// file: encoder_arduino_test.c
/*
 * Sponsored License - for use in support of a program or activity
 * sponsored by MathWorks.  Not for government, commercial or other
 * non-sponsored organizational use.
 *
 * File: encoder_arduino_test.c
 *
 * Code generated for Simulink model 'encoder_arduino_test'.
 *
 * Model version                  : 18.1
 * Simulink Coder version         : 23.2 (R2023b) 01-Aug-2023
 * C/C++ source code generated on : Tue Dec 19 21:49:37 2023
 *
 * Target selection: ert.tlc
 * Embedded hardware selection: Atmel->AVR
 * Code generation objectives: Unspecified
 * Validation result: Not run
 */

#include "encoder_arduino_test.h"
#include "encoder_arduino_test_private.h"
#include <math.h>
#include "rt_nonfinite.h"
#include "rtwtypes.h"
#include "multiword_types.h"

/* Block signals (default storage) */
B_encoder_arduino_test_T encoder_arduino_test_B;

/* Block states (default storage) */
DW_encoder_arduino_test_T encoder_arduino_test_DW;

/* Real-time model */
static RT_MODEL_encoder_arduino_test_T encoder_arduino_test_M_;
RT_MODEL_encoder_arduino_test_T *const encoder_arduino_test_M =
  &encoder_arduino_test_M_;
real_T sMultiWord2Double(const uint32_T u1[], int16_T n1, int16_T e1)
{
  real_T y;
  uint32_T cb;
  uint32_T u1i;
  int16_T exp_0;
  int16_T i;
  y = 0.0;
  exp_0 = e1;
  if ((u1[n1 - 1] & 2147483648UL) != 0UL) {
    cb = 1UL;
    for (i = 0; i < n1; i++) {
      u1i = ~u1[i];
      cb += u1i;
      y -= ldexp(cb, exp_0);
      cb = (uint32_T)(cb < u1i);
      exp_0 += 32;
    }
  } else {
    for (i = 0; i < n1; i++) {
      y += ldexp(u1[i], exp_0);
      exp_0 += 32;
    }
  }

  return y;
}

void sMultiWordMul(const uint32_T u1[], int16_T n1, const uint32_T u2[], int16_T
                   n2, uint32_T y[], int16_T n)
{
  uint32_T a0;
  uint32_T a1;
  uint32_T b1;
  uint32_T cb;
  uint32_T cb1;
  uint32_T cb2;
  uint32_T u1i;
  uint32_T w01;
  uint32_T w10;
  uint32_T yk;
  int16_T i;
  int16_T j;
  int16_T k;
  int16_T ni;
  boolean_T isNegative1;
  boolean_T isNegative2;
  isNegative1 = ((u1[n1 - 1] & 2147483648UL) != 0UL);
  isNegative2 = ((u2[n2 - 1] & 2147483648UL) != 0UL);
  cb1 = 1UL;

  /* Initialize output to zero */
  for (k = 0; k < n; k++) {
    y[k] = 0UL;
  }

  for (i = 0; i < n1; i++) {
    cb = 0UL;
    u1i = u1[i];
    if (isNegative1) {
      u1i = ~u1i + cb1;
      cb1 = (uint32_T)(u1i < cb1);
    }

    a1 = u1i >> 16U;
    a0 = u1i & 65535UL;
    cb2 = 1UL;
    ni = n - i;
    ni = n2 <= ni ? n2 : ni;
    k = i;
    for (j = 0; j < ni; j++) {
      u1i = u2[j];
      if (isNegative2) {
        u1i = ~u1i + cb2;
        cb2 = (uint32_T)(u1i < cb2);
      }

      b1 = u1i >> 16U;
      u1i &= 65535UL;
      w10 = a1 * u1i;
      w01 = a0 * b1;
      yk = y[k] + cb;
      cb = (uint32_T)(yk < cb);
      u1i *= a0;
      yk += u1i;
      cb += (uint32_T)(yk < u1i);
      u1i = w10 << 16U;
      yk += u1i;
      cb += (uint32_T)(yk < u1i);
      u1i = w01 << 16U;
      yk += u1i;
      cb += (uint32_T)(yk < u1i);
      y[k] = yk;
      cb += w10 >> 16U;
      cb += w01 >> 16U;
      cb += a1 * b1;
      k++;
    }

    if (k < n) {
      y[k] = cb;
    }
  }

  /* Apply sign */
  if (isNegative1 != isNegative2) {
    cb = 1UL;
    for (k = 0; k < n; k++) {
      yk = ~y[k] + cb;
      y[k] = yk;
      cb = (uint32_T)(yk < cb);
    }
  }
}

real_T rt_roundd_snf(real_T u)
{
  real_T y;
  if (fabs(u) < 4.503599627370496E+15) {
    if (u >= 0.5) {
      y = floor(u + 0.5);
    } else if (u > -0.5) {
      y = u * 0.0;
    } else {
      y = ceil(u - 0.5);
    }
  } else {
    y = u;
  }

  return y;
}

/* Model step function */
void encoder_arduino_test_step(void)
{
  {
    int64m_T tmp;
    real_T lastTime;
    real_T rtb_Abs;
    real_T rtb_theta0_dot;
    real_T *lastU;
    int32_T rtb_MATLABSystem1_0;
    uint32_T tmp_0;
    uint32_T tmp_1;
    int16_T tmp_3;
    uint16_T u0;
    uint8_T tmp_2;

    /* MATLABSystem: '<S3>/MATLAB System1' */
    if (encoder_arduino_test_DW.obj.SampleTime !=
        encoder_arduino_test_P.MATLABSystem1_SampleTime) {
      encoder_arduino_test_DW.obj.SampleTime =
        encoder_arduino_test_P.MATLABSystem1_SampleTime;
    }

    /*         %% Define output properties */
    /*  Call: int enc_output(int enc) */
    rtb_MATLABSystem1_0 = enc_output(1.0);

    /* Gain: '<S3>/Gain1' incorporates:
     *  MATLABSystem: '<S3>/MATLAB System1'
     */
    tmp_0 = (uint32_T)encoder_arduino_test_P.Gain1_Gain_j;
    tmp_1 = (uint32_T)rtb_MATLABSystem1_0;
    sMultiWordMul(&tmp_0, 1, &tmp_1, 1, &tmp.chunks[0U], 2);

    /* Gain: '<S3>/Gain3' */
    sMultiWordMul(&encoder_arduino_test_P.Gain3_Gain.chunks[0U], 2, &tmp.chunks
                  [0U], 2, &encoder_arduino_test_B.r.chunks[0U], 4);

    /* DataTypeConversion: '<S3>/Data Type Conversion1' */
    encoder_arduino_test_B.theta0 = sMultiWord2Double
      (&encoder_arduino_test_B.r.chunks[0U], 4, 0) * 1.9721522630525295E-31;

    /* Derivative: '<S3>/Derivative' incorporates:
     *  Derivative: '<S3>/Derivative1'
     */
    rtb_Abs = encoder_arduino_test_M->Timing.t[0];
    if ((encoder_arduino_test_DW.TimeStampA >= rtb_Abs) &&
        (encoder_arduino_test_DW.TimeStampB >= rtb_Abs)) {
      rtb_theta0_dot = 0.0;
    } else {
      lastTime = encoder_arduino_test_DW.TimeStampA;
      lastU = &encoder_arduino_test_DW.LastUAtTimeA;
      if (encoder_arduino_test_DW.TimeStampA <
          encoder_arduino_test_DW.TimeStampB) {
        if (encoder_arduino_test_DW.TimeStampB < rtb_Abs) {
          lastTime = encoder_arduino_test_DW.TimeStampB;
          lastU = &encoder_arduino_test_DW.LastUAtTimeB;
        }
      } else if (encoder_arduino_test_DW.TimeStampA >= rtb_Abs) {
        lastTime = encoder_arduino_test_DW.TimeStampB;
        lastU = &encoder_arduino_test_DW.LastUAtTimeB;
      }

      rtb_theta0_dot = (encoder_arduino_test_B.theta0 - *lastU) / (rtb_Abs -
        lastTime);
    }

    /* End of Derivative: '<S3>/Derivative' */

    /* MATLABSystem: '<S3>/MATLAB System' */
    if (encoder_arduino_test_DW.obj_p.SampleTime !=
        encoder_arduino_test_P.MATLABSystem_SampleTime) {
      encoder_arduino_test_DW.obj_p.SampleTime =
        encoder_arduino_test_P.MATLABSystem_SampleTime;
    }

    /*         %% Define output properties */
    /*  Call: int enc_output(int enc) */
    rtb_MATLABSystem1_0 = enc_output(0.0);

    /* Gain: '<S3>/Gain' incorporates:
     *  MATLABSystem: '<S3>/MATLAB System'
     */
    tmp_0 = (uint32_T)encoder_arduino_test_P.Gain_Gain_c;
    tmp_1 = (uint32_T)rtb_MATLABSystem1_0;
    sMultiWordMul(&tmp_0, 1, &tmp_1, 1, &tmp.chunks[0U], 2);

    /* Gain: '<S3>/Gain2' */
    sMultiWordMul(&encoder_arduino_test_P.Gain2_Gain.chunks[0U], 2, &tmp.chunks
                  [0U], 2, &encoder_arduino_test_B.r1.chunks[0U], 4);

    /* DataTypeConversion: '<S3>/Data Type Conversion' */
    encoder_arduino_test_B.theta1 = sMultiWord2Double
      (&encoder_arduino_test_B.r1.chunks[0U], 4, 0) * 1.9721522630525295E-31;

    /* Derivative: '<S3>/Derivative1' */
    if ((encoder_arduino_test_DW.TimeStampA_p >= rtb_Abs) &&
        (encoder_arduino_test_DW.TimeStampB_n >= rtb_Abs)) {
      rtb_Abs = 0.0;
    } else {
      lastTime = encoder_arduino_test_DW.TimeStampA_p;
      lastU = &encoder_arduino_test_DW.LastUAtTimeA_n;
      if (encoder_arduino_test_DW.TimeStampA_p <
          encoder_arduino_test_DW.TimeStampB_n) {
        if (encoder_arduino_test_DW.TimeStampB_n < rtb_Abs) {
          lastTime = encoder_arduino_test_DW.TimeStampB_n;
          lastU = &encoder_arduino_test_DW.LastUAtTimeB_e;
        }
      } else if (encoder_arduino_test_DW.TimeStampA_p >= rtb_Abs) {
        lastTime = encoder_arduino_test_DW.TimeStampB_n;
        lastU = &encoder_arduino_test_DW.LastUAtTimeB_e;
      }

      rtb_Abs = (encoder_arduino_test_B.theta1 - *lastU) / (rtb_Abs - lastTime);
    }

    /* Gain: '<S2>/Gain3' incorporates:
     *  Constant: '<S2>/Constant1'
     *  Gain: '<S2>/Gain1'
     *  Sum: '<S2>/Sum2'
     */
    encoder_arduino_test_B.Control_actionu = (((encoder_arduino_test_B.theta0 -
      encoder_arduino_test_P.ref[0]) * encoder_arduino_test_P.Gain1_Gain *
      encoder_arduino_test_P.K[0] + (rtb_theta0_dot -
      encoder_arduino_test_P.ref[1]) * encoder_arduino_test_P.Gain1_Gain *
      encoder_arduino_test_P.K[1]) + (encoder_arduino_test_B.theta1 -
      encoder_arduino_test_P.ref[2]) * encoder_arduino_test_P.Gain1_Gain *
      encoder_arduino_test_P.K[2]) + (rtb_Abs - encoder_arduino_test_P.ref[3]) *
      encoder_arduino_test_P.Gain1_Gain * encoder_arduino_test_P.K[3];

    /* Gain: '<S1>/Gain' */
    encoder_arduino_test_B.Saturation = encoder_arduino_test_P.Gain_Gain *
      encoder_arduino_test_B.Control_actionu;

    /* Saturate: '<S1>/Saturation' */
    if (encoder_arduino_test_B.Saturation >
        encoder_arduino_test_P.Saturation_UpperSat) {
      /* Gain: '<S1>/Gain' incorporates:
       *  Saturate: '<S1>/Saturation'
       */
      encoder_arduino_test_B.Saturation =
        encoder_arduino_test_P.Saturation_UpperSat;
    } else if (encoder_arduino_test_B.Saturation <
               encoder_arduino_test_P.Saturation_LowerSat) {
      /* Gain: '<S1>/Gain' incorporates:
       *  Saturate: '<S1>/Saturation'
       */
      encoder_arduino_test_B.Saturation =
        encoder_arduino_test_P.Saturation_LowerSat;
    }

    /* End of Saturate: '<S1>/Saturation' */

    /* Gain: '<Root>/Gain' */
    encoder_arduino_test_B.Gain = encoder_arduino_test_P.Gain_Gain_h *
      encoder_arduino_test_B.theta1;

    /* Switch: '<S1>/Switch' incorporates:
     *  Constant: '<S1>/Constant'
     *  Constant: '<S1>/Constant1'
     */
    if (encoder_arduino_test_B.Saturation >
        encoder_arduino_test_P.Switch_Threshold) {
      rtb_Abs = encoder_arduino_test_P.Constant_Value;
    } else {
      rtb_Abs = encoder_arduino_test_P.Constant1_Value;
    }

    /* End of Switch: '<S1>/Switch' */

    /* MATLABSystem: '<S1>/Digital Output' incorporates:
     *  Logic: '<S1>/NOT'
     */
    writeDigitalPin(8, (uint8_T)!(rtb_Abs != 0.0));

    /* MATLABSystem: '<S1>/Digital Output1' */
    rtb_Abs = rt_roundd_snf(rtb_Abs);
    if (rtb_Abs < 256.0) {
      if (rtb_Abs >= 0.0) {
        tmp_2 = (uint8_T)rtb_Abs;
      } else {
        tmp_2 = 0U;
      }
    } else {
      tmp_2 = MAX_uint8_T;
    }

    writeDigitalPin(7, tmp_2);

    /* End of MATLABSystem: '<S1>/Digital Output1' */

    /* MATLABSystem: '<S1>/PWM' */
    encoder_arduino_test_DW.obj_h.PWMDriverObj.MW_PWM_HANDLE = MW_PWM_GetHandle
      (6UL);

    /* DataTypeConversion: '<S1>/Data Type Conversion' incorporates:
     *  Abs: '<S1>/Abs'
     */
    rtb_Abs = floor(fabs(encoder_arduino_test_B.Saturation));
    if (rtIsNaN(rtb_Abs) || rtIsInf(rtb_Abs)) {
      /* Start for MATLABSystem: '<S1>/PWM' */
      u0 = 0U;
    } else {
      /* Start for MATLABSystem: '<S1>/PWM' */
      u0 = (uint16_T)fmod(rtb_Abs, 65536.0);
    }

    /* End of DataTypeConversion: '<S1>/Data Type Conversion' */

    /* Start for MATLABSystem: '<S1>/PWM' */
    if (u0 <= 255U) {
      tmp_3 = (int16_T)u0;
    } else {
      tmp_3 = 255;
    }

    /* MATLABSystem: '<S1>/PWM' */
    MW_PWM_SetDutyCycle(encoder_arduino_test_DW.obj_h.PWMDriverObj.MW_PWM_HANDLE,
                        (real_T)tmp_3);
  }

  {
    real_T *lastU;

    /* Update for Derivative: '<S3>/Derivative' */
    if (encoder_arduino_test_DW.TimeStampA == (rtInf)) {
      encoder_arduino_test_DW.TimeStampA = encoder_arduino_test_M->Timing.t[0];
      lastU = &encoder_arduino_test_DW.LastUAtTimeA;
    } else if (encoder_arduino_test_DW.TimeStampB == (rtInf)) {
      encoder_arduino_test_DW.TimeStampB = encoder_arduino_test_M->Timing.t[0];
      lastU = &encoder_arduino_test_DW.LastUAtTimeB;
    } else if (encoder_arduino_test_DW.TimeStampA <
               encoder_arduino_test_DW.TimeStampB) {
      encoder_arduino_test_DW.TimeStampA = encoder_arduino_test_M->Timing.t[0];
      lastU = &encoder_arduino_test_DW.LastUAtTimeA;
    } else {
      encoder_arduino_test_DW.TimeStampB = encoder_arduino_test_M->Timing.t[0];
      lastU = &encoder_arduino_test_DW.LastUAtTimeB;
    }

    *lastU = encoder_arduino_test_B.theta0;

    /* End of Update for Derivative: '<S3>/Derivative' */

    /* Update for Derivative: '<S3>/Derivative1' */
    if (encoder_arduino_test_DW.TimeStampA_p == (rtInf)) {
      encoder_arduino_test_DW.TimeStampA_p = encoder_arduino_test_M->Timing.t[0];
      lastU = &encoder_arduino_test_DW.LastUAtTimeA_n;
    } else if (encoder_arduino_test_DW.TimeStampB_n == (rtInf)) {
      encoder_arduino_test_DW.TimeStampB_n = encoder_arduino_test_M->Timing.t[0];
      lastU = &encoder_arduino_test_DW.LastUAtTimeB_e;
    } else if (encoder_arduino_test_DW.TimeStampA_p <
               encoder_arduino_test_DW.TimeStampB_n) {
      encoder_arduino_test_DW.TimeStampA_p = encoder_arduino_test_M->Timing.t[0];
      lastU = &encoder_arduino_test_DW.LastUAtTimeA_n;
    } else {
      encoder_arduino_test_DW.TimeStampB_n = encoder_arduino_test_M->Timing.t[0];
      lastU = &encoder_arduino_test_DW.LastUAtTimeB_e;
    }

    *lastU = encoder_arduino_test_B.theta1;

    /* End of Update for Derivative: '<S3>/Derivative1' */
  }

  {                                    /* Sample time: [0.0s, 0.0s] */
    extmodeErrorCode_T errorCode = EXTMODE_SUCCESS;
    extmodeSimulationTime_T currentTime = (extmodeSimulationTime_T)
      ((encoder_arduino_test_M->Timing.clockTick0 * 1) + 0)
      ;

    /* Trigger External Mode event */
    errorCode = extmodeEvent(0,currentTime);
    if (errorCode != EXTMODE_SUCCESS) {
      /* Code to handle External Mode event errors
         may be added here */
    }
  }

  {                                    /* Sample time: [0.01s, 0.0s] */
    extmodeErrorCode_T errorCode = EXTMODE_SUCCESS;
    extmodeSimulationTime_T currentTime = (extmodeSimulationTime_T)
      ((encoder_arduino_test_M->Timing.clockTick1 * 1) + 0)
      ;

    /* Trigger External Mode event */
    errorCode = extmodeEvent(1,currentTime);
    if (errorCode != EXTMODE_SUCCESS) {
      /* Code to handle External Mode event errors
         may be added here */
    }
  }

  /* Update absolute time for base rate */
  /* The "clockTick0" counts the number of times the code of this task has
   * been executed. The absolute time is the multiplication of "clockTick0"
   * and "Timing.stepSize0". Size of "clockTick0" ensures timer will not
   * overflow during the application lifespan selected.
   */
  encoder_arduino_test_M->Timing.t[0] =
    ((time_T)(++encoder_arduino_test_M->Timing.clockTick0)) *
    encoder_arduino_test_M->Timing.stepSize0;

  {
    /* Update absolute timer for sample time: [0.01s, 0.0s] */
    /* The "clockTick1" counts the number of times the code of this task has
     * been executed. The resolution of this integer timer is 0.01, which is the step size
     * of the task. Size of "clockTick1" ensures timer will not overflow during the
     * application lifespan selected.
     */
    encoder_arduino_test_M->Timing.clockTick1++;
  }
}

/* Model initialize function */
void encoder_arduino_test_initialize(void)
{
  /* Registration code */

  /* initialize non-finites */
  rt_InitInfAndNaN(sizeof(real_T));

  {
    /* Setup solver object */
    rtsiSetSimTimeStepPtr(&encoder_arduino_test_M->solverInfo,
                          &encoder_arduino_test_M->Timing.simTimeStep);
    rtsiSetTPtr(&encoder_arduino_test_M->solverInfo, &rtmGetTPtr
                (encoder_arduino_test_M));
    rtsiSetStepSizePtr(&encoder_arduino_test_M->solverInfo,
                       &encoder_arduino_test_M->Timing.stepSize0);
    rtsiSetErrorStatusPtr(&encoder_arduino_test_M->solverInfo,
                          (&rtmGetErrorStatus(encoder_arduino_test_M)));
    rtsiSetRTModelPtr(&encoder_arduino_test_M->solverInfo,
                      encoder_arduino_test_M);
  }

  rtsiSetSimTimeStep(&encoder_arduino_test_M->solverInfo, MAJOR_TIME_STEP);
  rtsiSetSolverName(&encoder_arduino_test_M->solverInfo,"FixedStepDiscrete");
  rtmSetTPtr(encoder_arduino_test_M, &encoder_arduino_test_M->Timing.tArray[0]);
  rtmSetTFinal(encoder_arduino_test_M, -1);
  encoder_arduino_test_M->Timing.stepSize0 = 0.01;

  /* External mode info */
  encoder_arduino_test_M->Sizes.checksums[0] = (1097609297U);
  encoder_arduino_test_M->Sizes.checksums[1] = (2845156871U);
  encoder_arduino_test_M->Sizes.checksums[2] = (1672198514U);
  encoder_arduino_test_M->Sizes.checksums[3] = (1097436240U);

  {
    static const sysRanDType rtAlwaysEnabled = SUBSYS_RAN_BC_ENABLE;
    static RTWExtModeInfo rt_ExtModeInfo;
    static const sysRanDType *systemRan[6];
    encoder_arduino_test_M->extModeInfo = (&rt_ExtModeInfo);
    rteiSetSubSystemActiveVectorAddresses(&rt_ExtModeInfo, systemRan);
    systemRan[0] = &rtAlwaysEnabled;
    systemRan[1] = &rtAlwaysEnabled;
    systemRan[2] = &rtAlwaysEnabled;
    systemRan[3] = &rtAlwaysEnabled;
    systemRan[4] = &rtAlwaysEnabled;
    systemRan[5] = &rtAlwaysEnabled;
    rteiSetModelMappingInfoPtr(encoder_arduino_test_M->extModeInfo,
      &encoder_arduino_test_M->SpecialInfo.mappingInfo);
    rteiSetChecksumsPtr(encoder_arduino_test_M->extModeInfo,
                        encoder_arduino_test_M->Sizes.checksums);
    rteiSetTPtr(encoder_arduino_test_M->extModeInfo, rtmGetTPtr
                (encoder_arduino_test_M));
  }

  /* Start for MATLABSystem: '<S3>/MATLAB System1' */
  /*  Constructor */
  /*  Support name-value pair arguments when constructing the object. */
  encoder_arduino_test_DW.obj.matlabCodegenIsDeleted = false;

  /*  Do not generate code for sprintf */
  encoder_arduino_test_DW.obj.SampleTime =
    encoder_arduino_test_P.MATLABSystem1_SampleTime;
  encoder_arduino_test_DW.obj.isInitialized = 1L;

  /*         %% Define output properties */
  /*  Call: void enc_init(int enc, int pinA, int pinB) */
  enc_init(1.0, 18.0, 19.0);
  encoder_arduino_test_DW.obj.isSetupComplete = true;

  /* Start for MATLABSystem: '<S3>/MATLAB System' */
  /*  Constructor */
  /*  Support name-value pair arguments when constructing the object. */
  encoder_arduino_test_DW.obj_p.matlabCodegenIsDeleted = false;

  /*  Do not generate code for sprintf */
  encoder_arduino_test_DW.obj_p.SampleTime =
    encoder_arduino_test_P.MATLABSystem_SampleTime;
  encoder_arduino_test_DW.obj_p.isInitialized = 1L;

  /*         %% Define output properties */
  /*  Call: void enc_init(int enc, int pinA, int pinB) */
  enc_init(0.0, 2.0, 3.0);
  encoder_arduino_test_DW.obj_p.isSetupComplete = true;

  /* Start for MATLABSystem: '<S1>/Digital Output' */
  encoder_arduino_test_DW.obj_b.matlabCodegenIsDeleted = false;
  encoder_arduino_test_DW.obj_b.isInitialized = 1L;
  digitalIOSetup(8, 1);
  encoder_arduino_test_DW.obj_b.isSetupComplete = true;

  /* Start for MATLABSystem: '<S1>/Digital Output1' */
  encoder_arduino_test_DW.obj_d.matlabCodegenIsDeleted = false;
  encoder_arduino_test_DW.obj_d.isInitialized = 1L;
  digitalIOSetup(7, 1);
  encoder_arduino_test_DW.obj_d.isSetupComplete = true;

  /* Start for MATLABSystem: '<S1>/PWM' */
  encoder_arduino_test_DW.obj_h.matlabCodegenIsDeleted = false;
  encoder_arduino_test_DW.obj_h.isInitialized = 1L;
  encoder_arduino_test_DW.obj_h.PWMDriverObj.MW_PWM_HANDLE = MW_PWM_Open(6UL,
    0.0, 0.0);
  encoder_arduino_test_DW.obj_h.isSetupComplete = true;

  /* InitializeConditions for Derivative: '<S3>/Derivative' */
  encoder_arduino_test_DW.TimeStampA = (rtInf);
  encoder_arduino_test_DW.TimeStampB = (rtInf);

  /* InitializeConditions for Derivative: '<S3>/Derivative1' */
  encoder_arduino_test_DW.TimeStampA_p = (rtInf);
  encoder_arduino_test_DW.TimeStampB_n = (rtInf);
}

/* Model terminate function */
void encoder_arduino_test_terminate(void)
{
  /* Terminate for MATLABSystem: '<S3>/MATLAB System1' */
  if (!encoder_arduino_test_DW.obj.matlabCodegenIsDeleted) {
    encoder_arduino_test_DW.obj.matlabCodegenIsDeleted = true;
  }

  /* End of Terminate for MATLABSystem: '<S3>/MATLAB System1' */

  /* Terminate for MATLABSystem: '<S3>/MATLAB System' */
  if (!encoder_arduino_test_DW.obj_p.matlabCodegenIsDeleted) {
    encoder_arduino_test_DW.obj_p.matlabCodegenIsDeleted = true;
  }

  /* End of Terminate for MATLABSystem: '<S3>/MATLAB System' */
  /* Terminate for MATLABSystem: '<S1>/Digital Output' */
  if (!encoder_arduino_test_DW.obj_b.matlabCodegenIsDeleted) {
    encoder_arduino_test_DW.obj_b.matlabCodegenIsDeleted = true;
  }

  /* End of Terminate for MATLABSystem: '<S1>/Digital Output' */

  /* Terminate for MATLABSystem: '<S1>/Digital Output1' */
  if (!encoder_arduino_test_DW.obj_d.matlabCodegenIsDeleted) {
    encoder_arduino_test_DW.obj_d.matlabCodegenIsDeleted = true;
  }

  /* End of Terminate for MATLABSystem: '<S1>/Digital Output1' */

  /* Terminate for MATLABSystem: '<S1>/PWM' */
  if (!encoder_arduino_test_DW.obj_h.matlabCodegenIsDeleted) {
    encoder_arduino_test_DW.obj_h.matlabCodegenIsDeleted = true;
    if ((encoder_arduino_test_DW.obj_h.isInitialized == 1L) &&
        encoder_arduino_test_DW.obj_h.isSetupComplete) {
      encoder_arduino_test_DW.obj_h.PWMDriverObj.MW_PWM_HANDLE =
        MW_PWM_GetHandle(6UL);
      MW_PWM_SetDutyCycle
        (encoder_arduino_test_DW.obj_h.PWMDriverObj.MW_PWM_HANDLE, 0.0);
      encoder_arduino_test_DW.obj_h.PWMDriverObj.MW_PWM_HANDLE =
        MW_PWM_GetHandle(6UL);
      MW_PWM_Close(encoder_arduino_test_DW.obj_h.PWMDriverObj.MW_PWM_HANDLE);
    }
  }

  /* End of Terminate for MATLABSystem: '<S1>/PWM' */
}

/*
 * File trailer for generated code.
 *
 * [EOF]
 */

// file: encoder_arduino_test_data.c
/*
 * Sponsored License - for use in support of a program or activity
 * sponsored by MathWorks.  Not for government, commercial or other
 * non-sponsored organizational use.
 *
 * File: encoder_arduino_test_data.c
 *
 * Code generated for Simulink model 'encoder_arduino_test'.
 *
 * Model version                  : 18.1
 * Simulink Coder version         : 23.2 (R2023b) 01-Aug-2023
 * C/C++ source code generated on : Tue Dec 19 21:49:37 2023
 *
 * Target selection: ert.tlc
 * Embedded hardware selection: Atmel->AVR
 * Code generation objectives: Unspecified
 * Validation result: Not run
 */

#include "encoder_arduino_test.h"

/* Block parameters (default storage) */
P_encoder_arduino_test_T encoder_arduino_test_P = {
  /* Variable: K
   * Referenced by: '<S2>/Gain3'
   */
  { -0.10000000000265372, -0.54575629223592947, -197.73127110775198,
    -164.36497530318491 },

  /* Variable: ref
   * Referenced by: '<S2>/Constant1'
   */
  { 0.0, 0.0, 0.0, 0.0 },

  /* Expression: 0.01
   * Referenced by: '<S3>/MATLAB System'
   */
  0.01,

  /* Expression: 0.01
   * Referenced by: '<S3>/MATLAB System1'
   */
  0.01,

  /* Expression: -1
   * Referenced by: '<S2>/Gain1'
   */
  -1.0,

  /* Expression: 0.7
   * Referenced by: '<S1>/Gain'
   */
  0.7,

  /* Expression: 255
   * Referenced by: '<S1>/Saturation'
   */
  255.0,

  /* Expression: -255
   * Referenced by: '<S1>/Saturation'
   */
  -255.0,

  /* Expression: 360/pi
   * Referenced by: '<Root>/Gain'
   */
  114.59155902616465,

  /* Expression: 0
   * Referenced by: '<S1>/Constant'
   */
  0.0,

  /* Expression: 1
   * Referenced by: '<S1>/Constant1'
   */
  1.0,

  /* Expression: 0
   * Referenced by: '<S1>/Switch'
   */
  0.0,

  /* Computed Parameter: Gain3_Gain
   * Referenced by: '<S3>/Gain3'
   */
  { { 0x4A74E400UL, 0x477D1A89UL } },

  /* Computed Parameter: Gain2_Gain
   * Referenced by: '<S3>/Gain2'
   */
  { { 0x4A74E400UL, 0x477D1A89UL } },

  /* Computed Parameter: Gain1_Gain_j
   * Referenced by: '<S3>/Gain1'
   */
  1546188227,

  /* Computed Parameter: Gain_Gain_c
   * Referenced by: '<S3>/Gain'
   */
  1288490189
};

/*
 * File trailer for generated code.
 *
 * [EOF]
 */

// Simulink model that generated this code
simulink model "encoder_arduino_test"  (R2023b)
settings: Solver=ode3  StartTime=0.0  StopTime=inf  FixedStep=0.01  RelTol=1e-3  EnableMultiTasking=on
undefined symbols (not defined in the file): K, ref
libraries: arduinolib x3

== system encoder_arduino_test ==
  Arduino harduare drive : Subsystem
  Controller : Subsystem
  Demux : Demux
  Gain : Gain  Gain=360/pi
  Scope : Scope  NumInputPorts=2
  States Reading : Subsystem
  wires:
  States Reading/1(State Vector X) -> Demux/1, Controller/1(State Vector X)  "State Vector X"
  Controller/1(Contro Action u) -> Arduino harduare drive/1(Contro Action u)
  Arduino harduare drive/1(Signed Pwm) -> Scope/1
  Demux/3 -> Gain/1
  Gain/1 -> Scope/2

== system encoder_arduino_test/Arduino harduare drive ==
  note: zero
  Contro Action u : Inport
  Abs : Abs  SaturateOnIntegerOverflow=off
  Constant : Constant  Value=0
  Constant1 : Constant
  Data Type Conversion : DataTypeConversion  OutDataTypeStr=uint16  SaturateOnIntegerOverflow=off  RndMeth=Floor
  Digital Output : arduinolib/Digital Output  pinNumber=8  Direction=output  blockPlatform=arduino
  Digital Output1 : arduinolib/Digital Output  pinNumber=7  Direction=output  blockPlatform=arduino
  Gain : Gain  Gain=0.7
  NOT : Logic  Operator=NOT  IconShape=distinctive  AllPortsSameDT=off  OutDataTypeStr=boolean
  PWM : arduinolib/PWM  pinNumber=6  frequencyType=Default  desiredFrequency=490.2  achievableFrequency=490.2
  Saturation : Saturate  UpperLimit=255  LowerLimit=-255
  Scope : Scope
  Switch : Switch  Criteria=u2 > Threshold  SaturateOnIntegerOverflow=off  InputSameDT=off
  Signed Pwm : Outport
  wires:
  Contro Action u/1 -> Scope/1, Gain/1
  Saturation/1 -> Signed Pwm/1, Abs/1, Switch/2
  Constant/1 -> Switch/1
  Constant1/1 -> Switch/3
  NOT/1 -> Digital Output/1
  Switch/1 -> Digital Output1/1, NOT/1
  Abs/1 -> Data Type Conversion/1
  Gain/1 -> Saturation/1
  Data Type Conversion/1 -> PWM/1

== system encoder_arduino_test/Controller ==
  note: u=-K (X - ref)
  State Vector X : Inport
  Constant1 : Constant  Value=ref
  Gain1 : Gain  Gain=-1
  Gain3 : Gain  Gain=K  Multiplication=Matrix(K*u)
  Sum2 : Sum  Inputs=|+-
  Contro Action u : Outport
  wires:
  Constant1/1 -> Sum2/2
  Sum2/1 -> Gain1/1
  State Vector X/1 -> Sum2/1
  Gain3/1 -> Contro Action u/1  "Control_action u"
  Gain1/1 -> Gain3/1

== system encoder_arduino_test/States Reading ==
  Data Type Conversion : DataTypeConversion  OutDataTypeStr=double  SaturateOnIntegerOverflow=off  RndMeth=Floor
  Data Type Conversion1 : DataTypeConversion  OutDataTypeStr=double  SaturateOnIntegerOverflow=off  RndMeth=Floor
  Derivative : Derivative
  Derivative1 : Derivative
  Gain : Gain  Gain=180/1200
  Gain1 : Gain  Gain=180/1000
  Gain2 : Gain  Gain=pi/360
  Gain3 : Gain  Gain=pi/360
  MATLAB System : MATLABSystem  System=Encoder_arduino  Encoder=0  PinA=2  PinB=3  SampleTime=0.01
  MATLAB System1 : MATLABSystem  System=Encoder_arduino  Encoder=1  PinA=18  PinB=19  SampleTime=0.01
  Mux : Mux
  State Vector X : Outport
  wires:
  MATLAB System1/1 -> Gain1/1
  Data Type Conversion1/1 -> Derivative/1, Mux/1  "theta0"
  Gain/1 -> Gain2/1
  Derivative/1 -> Mux/2  "theta0_dot"
  MATLAB System/1 -> Gain/1
  Derivative1/1 -> Mux/4  "theta1_dot"
  Data Type Conversion/1 -> Derivative1/1, Mux/3  "theta1"
  Gain1/1 -> Gain3/1
  Gain2/1 -> Data Type Conversion/1  "theta1"
  Gain3/1 -> Data Type Conversion1/1  "theta0"
  Mux/1 -> State Vector X/1  "State Vector X"
